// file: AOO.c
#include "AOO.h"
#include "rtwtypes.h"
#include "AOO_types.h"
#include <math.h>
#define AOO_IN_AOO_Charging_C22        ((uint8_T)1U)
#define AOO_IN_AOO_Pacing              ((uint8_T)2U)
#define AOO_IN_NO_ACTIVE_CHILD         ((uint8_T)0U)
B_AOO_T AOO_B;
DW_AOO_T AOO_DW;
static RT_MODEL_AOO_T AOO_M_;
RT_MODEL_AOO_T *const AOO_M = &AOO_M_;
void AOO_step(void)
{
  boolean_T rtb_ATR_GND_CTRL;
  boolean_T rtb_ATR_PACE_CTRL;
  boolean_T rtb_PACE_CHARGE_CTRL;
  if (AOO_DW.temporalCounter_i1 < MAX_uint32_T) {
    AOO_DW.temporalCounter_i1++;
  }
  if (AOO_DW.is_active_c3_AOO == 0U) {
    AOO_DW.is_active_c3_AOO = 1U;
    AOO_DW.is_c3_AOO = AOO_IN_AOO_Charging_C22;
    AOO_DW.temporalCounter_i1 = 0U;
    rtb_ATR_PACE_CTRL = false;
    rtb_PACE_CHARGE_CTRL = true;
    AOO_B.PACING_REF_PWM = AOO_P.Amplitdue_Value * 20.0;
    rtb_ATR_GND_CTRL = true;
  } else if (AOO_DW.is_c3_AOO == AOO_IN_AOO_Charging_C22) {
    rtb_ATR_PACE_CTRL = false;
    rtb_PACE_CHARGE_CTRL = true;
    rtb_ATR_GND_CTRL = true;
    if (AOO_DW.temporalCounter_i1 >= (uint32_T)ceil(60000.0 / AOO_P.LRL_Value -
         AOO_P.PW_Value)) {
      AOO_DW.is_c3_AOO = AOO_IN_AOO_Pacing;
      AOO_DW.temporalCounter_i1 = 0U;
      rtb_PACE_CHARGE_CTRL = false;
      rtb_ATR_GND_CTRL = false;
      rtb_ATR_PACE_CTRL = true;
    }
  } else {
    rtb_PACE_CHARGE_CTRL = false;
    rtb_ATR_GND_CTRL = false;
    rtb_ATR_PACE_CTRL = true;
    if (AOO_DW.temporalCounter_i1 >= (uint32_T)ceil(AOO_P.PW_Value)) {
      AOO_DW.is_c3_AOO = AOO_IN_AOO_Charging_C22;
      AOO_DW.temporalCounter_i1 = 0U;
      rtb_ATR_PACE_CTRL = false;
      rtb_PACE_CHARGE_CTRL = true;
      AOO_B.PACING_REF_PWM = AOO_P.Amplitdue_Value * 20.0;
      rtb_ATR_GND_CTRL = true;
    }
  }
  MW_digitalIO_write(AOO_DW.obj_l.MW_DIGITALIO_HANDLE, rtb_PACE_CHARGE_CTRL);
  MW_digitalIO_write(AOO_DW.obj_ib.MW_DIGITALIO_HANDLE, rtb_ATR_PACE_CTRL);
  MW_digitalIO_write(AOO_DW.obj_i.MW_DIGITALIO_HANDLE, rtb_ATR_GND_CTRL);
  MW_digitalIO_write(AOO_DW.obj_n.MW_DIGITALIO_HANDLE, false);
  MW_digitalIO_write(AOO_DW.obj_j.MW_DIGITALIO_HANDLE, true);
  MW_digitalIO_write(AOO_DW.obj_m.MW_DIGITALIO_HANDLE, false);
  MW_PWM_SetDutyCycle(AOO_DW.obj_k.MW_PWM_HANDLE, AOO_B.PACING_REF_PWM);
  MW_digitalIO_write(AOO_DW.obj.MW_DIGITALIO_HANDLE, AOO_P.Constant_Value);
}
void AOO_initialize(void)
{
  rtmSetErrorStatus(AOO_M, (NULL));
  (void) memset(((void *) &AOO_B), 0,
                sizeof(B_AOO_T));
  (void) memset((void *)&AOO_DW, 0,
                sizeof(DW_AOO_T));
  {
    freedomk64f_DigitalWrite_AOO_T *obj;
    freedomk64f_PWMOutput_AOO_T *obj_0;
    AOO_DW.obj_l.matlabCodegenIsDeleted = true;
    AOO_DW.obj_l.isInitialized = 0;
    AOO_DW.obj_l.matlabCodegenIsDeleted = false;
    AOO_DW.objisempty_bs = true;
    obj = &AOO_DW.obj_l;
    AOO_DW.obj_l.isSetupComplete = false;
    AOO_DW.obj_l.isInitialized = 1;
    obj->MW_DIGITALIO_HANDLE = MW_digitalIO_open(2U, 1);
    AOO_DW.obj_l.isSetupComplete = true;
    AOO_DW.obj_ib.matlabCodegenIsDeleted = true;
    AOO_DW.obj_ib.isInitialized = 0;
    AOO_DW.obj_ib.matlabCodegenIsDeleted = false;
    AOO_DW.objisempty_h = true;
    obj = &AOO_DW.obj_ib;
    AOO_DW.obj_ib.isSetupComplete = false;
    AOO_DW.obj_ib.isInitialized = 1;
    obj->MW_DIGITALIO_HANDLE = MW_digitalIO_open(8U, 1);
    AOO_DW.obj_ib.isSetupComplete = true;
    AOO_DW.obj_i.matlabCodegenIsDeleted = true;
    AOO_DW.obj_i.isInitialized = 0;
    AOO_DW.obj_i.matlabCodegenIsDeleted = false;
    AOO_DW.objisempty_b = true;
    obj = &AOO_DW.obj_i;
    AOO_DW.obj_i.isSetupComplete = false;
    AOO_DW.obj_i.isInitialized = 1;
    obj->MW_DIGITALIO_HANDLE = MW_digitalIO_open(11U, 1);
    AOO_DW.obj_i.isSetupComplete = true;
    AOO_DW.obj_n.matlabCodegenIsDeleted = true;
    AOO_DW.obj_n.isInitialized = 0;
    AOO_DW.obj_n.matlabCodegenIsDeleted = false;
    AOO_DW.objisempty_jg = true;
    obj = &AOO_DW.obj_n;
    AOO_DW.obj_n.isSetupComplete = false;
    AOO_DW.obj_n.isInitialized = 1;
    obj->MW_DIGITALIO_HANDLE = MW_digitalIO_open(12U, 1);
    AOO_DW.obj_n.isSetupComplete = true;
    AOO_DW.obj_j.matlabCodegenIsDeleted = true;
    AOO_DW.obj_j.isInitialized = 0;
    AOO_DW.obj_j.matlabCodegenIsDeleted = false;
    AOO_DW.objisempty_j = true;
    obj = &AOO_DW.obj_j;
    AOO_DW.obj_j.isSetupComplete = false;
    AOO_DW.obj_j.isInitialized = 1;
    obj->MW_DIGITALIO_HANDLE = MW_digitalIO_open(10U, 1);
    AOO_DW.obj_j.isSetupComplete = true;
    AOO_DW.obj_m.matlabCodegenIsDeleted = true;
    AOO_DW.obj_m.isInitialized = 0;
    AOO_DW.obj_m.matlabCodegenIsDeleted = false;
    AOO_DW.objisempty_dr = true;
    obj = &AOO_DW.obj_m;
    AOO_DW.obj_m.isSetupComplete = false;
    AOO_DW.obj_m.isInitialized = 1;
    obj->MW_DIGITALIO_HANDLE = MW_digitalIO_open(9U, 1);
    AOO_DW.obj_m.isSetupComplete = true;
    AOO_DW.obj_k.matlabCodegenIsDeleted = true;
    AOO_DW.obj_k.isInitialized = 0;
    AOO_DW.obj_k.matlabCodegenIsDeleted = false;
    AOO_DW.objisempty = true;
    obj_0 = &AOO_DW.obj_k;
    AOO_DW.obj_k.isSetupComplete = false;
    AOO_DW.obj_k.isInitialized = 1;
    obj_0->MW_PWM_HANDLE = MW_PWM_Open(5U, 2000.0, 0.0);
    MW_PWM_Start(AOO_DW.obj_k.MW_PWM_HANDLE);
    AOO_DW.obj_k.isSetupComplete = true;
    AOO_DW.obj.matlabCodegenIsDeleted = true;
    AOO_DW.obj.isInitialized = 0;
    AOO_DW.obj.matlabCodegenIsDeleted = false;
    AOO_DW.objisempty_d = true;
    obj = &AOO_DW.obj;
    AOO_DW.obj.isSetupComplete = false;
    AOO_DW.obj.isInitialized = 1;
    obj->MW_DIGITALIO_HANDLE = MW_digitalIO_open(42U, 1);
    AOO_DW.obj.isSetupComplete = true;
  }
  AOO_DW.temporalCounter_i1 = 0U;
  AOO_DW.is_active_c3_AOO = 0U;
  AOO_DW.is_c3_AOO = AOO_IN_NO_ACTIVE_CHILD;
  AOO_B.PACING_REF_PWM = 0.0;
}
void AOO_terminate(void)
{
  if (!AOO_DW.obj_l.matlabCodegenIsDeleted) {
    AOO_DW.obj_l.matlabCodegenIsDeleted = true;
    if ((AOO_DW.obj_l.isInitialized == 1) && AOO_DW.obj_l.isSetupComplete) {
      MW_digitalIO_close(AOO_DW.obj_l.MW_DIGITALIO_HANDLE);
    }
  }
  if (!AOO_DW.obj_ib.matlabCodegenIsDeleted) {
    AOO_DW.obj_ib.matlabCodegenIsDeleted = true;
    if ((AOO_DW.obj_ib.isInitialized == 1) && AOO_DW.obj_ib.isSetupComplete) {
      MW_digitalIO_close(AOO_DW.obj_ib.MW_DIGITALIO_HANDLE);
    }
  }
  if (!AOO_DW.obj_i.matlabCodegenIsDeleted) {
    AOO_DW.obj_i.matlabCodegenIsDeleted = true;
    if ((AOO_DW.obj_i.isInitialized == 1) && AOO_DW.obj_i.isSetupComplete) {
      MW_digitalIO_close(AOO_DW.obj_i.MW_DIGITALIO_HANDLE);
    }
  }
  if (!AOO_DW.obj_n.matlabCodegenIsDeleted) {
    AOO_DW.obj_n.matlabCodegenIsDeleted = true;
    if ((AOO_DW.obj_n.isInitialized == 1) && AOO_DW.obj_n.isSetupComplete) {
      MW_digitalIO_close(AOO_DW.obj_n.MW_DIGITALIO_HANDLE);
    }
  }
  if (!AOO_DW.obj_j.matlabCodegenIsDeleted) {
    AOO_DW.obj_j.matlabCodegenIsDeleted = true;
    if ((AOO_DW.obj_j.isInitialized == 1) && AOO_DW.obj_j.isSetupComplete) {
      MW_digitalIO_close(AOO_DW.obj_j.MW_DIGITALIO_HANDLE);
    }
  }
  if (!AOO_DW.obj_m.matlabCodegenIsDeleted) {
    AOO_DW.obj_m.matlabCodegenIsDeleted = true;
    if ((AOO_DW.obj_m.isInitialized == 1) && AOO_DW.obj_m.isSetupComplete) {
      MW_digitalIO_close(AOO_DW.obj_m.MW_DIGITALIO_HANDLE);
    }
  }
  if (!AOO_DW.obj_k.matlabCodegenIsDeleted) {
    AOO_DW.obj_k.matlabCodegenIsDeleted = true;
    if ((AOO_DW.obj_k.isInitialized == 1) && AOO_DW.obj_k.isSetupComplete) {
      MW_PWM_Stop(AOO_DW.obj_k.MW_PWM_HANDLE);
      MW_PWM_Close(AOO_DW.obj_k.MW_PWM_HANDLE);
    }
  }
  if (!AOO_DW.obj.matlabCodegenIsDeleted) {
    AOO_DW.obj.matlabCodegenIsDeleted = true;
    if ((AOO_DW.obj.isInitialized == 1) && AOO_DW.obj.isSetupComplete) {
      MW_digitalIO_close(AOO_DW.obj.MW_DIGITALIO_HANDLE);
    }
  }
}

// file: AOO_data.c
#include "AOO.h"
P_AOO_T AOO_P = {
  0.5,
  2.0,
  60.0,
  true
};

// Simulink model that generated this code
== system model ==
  DigitalWrite : frdmk64flib/Digital Write  <- 1: Stateflowchart#1/3
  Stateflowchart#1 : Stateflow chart  <- 1: PW, 2: Amplitdue, 3: LRL
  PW : Constant  Value=0.5
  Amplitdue : Constant  Value=2
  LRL : Constant  Value=60
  DigitalWrite#1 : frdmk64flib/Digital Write  <- 1: Stateflowchart#1/2
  DigitalWrite#2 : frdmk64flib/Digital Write  <- 1: Stateflowchart#1
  DigitalWrite#3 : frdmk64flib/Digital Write  <- 1: Stateflowchart#1/4
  DigitalWrite#4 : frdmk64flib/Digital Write  <- 1: Stateflowchart#1/6
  DigitalWrite#5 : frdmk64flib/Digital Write  <- 1: Stateflowchart#1/5
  PWMOutput : frdmk64flib/PWM Output  <- 1: Stateflowchart#1/7
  DigitalWrite#6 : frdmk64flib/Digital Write  <- 1: Constant
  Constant : Constant  Value=true
== stateflow chart Stateflowchart#1 ==
  state AOO_Charging_C22
    entry:
    VENT_PACE_CTRL = false;
    ATR_PACE_CTRL = false;
    PACE_CHARGE_CTRL = true;
    PACING_REF_PWM = Amplitude * 20;
    PACE_GND_CTRL= true;
    VENT_GND_CTRL = false;
    ATR_GND_CTRL = true;
  state AOO_Pacing
    entry:
    PACE_CHARGE_CTRL = false;
    PACE_GND_CTRL = true;
    VENT_PACE_CTRL = false;
    VENT_GND_CTRL = false;
    ATR_GND_CTRL = false;
    ATR_PACE_CTRL = true;
  (default) -> AOO_Charging_C22
  AOO_Charging_C22 -> AOO_Pacing : after(((60000/LRL) - PW), msec)
  AOO_Pacing -> AOO_Charging_C22 : after(PW, msec)
  data: ATR_GND_CTRL output boolean; ATR_PACE_CTRL output boolean; PACE_CHARGE_CTRL output boolean; VENT_GND_CTRL output boolean; VENT_PACE_CTRL output boolean; PACE_GND_CTRL output boolean; PW input double; Amplitude input double; LRL input double; PACING_REF_PWM output double
